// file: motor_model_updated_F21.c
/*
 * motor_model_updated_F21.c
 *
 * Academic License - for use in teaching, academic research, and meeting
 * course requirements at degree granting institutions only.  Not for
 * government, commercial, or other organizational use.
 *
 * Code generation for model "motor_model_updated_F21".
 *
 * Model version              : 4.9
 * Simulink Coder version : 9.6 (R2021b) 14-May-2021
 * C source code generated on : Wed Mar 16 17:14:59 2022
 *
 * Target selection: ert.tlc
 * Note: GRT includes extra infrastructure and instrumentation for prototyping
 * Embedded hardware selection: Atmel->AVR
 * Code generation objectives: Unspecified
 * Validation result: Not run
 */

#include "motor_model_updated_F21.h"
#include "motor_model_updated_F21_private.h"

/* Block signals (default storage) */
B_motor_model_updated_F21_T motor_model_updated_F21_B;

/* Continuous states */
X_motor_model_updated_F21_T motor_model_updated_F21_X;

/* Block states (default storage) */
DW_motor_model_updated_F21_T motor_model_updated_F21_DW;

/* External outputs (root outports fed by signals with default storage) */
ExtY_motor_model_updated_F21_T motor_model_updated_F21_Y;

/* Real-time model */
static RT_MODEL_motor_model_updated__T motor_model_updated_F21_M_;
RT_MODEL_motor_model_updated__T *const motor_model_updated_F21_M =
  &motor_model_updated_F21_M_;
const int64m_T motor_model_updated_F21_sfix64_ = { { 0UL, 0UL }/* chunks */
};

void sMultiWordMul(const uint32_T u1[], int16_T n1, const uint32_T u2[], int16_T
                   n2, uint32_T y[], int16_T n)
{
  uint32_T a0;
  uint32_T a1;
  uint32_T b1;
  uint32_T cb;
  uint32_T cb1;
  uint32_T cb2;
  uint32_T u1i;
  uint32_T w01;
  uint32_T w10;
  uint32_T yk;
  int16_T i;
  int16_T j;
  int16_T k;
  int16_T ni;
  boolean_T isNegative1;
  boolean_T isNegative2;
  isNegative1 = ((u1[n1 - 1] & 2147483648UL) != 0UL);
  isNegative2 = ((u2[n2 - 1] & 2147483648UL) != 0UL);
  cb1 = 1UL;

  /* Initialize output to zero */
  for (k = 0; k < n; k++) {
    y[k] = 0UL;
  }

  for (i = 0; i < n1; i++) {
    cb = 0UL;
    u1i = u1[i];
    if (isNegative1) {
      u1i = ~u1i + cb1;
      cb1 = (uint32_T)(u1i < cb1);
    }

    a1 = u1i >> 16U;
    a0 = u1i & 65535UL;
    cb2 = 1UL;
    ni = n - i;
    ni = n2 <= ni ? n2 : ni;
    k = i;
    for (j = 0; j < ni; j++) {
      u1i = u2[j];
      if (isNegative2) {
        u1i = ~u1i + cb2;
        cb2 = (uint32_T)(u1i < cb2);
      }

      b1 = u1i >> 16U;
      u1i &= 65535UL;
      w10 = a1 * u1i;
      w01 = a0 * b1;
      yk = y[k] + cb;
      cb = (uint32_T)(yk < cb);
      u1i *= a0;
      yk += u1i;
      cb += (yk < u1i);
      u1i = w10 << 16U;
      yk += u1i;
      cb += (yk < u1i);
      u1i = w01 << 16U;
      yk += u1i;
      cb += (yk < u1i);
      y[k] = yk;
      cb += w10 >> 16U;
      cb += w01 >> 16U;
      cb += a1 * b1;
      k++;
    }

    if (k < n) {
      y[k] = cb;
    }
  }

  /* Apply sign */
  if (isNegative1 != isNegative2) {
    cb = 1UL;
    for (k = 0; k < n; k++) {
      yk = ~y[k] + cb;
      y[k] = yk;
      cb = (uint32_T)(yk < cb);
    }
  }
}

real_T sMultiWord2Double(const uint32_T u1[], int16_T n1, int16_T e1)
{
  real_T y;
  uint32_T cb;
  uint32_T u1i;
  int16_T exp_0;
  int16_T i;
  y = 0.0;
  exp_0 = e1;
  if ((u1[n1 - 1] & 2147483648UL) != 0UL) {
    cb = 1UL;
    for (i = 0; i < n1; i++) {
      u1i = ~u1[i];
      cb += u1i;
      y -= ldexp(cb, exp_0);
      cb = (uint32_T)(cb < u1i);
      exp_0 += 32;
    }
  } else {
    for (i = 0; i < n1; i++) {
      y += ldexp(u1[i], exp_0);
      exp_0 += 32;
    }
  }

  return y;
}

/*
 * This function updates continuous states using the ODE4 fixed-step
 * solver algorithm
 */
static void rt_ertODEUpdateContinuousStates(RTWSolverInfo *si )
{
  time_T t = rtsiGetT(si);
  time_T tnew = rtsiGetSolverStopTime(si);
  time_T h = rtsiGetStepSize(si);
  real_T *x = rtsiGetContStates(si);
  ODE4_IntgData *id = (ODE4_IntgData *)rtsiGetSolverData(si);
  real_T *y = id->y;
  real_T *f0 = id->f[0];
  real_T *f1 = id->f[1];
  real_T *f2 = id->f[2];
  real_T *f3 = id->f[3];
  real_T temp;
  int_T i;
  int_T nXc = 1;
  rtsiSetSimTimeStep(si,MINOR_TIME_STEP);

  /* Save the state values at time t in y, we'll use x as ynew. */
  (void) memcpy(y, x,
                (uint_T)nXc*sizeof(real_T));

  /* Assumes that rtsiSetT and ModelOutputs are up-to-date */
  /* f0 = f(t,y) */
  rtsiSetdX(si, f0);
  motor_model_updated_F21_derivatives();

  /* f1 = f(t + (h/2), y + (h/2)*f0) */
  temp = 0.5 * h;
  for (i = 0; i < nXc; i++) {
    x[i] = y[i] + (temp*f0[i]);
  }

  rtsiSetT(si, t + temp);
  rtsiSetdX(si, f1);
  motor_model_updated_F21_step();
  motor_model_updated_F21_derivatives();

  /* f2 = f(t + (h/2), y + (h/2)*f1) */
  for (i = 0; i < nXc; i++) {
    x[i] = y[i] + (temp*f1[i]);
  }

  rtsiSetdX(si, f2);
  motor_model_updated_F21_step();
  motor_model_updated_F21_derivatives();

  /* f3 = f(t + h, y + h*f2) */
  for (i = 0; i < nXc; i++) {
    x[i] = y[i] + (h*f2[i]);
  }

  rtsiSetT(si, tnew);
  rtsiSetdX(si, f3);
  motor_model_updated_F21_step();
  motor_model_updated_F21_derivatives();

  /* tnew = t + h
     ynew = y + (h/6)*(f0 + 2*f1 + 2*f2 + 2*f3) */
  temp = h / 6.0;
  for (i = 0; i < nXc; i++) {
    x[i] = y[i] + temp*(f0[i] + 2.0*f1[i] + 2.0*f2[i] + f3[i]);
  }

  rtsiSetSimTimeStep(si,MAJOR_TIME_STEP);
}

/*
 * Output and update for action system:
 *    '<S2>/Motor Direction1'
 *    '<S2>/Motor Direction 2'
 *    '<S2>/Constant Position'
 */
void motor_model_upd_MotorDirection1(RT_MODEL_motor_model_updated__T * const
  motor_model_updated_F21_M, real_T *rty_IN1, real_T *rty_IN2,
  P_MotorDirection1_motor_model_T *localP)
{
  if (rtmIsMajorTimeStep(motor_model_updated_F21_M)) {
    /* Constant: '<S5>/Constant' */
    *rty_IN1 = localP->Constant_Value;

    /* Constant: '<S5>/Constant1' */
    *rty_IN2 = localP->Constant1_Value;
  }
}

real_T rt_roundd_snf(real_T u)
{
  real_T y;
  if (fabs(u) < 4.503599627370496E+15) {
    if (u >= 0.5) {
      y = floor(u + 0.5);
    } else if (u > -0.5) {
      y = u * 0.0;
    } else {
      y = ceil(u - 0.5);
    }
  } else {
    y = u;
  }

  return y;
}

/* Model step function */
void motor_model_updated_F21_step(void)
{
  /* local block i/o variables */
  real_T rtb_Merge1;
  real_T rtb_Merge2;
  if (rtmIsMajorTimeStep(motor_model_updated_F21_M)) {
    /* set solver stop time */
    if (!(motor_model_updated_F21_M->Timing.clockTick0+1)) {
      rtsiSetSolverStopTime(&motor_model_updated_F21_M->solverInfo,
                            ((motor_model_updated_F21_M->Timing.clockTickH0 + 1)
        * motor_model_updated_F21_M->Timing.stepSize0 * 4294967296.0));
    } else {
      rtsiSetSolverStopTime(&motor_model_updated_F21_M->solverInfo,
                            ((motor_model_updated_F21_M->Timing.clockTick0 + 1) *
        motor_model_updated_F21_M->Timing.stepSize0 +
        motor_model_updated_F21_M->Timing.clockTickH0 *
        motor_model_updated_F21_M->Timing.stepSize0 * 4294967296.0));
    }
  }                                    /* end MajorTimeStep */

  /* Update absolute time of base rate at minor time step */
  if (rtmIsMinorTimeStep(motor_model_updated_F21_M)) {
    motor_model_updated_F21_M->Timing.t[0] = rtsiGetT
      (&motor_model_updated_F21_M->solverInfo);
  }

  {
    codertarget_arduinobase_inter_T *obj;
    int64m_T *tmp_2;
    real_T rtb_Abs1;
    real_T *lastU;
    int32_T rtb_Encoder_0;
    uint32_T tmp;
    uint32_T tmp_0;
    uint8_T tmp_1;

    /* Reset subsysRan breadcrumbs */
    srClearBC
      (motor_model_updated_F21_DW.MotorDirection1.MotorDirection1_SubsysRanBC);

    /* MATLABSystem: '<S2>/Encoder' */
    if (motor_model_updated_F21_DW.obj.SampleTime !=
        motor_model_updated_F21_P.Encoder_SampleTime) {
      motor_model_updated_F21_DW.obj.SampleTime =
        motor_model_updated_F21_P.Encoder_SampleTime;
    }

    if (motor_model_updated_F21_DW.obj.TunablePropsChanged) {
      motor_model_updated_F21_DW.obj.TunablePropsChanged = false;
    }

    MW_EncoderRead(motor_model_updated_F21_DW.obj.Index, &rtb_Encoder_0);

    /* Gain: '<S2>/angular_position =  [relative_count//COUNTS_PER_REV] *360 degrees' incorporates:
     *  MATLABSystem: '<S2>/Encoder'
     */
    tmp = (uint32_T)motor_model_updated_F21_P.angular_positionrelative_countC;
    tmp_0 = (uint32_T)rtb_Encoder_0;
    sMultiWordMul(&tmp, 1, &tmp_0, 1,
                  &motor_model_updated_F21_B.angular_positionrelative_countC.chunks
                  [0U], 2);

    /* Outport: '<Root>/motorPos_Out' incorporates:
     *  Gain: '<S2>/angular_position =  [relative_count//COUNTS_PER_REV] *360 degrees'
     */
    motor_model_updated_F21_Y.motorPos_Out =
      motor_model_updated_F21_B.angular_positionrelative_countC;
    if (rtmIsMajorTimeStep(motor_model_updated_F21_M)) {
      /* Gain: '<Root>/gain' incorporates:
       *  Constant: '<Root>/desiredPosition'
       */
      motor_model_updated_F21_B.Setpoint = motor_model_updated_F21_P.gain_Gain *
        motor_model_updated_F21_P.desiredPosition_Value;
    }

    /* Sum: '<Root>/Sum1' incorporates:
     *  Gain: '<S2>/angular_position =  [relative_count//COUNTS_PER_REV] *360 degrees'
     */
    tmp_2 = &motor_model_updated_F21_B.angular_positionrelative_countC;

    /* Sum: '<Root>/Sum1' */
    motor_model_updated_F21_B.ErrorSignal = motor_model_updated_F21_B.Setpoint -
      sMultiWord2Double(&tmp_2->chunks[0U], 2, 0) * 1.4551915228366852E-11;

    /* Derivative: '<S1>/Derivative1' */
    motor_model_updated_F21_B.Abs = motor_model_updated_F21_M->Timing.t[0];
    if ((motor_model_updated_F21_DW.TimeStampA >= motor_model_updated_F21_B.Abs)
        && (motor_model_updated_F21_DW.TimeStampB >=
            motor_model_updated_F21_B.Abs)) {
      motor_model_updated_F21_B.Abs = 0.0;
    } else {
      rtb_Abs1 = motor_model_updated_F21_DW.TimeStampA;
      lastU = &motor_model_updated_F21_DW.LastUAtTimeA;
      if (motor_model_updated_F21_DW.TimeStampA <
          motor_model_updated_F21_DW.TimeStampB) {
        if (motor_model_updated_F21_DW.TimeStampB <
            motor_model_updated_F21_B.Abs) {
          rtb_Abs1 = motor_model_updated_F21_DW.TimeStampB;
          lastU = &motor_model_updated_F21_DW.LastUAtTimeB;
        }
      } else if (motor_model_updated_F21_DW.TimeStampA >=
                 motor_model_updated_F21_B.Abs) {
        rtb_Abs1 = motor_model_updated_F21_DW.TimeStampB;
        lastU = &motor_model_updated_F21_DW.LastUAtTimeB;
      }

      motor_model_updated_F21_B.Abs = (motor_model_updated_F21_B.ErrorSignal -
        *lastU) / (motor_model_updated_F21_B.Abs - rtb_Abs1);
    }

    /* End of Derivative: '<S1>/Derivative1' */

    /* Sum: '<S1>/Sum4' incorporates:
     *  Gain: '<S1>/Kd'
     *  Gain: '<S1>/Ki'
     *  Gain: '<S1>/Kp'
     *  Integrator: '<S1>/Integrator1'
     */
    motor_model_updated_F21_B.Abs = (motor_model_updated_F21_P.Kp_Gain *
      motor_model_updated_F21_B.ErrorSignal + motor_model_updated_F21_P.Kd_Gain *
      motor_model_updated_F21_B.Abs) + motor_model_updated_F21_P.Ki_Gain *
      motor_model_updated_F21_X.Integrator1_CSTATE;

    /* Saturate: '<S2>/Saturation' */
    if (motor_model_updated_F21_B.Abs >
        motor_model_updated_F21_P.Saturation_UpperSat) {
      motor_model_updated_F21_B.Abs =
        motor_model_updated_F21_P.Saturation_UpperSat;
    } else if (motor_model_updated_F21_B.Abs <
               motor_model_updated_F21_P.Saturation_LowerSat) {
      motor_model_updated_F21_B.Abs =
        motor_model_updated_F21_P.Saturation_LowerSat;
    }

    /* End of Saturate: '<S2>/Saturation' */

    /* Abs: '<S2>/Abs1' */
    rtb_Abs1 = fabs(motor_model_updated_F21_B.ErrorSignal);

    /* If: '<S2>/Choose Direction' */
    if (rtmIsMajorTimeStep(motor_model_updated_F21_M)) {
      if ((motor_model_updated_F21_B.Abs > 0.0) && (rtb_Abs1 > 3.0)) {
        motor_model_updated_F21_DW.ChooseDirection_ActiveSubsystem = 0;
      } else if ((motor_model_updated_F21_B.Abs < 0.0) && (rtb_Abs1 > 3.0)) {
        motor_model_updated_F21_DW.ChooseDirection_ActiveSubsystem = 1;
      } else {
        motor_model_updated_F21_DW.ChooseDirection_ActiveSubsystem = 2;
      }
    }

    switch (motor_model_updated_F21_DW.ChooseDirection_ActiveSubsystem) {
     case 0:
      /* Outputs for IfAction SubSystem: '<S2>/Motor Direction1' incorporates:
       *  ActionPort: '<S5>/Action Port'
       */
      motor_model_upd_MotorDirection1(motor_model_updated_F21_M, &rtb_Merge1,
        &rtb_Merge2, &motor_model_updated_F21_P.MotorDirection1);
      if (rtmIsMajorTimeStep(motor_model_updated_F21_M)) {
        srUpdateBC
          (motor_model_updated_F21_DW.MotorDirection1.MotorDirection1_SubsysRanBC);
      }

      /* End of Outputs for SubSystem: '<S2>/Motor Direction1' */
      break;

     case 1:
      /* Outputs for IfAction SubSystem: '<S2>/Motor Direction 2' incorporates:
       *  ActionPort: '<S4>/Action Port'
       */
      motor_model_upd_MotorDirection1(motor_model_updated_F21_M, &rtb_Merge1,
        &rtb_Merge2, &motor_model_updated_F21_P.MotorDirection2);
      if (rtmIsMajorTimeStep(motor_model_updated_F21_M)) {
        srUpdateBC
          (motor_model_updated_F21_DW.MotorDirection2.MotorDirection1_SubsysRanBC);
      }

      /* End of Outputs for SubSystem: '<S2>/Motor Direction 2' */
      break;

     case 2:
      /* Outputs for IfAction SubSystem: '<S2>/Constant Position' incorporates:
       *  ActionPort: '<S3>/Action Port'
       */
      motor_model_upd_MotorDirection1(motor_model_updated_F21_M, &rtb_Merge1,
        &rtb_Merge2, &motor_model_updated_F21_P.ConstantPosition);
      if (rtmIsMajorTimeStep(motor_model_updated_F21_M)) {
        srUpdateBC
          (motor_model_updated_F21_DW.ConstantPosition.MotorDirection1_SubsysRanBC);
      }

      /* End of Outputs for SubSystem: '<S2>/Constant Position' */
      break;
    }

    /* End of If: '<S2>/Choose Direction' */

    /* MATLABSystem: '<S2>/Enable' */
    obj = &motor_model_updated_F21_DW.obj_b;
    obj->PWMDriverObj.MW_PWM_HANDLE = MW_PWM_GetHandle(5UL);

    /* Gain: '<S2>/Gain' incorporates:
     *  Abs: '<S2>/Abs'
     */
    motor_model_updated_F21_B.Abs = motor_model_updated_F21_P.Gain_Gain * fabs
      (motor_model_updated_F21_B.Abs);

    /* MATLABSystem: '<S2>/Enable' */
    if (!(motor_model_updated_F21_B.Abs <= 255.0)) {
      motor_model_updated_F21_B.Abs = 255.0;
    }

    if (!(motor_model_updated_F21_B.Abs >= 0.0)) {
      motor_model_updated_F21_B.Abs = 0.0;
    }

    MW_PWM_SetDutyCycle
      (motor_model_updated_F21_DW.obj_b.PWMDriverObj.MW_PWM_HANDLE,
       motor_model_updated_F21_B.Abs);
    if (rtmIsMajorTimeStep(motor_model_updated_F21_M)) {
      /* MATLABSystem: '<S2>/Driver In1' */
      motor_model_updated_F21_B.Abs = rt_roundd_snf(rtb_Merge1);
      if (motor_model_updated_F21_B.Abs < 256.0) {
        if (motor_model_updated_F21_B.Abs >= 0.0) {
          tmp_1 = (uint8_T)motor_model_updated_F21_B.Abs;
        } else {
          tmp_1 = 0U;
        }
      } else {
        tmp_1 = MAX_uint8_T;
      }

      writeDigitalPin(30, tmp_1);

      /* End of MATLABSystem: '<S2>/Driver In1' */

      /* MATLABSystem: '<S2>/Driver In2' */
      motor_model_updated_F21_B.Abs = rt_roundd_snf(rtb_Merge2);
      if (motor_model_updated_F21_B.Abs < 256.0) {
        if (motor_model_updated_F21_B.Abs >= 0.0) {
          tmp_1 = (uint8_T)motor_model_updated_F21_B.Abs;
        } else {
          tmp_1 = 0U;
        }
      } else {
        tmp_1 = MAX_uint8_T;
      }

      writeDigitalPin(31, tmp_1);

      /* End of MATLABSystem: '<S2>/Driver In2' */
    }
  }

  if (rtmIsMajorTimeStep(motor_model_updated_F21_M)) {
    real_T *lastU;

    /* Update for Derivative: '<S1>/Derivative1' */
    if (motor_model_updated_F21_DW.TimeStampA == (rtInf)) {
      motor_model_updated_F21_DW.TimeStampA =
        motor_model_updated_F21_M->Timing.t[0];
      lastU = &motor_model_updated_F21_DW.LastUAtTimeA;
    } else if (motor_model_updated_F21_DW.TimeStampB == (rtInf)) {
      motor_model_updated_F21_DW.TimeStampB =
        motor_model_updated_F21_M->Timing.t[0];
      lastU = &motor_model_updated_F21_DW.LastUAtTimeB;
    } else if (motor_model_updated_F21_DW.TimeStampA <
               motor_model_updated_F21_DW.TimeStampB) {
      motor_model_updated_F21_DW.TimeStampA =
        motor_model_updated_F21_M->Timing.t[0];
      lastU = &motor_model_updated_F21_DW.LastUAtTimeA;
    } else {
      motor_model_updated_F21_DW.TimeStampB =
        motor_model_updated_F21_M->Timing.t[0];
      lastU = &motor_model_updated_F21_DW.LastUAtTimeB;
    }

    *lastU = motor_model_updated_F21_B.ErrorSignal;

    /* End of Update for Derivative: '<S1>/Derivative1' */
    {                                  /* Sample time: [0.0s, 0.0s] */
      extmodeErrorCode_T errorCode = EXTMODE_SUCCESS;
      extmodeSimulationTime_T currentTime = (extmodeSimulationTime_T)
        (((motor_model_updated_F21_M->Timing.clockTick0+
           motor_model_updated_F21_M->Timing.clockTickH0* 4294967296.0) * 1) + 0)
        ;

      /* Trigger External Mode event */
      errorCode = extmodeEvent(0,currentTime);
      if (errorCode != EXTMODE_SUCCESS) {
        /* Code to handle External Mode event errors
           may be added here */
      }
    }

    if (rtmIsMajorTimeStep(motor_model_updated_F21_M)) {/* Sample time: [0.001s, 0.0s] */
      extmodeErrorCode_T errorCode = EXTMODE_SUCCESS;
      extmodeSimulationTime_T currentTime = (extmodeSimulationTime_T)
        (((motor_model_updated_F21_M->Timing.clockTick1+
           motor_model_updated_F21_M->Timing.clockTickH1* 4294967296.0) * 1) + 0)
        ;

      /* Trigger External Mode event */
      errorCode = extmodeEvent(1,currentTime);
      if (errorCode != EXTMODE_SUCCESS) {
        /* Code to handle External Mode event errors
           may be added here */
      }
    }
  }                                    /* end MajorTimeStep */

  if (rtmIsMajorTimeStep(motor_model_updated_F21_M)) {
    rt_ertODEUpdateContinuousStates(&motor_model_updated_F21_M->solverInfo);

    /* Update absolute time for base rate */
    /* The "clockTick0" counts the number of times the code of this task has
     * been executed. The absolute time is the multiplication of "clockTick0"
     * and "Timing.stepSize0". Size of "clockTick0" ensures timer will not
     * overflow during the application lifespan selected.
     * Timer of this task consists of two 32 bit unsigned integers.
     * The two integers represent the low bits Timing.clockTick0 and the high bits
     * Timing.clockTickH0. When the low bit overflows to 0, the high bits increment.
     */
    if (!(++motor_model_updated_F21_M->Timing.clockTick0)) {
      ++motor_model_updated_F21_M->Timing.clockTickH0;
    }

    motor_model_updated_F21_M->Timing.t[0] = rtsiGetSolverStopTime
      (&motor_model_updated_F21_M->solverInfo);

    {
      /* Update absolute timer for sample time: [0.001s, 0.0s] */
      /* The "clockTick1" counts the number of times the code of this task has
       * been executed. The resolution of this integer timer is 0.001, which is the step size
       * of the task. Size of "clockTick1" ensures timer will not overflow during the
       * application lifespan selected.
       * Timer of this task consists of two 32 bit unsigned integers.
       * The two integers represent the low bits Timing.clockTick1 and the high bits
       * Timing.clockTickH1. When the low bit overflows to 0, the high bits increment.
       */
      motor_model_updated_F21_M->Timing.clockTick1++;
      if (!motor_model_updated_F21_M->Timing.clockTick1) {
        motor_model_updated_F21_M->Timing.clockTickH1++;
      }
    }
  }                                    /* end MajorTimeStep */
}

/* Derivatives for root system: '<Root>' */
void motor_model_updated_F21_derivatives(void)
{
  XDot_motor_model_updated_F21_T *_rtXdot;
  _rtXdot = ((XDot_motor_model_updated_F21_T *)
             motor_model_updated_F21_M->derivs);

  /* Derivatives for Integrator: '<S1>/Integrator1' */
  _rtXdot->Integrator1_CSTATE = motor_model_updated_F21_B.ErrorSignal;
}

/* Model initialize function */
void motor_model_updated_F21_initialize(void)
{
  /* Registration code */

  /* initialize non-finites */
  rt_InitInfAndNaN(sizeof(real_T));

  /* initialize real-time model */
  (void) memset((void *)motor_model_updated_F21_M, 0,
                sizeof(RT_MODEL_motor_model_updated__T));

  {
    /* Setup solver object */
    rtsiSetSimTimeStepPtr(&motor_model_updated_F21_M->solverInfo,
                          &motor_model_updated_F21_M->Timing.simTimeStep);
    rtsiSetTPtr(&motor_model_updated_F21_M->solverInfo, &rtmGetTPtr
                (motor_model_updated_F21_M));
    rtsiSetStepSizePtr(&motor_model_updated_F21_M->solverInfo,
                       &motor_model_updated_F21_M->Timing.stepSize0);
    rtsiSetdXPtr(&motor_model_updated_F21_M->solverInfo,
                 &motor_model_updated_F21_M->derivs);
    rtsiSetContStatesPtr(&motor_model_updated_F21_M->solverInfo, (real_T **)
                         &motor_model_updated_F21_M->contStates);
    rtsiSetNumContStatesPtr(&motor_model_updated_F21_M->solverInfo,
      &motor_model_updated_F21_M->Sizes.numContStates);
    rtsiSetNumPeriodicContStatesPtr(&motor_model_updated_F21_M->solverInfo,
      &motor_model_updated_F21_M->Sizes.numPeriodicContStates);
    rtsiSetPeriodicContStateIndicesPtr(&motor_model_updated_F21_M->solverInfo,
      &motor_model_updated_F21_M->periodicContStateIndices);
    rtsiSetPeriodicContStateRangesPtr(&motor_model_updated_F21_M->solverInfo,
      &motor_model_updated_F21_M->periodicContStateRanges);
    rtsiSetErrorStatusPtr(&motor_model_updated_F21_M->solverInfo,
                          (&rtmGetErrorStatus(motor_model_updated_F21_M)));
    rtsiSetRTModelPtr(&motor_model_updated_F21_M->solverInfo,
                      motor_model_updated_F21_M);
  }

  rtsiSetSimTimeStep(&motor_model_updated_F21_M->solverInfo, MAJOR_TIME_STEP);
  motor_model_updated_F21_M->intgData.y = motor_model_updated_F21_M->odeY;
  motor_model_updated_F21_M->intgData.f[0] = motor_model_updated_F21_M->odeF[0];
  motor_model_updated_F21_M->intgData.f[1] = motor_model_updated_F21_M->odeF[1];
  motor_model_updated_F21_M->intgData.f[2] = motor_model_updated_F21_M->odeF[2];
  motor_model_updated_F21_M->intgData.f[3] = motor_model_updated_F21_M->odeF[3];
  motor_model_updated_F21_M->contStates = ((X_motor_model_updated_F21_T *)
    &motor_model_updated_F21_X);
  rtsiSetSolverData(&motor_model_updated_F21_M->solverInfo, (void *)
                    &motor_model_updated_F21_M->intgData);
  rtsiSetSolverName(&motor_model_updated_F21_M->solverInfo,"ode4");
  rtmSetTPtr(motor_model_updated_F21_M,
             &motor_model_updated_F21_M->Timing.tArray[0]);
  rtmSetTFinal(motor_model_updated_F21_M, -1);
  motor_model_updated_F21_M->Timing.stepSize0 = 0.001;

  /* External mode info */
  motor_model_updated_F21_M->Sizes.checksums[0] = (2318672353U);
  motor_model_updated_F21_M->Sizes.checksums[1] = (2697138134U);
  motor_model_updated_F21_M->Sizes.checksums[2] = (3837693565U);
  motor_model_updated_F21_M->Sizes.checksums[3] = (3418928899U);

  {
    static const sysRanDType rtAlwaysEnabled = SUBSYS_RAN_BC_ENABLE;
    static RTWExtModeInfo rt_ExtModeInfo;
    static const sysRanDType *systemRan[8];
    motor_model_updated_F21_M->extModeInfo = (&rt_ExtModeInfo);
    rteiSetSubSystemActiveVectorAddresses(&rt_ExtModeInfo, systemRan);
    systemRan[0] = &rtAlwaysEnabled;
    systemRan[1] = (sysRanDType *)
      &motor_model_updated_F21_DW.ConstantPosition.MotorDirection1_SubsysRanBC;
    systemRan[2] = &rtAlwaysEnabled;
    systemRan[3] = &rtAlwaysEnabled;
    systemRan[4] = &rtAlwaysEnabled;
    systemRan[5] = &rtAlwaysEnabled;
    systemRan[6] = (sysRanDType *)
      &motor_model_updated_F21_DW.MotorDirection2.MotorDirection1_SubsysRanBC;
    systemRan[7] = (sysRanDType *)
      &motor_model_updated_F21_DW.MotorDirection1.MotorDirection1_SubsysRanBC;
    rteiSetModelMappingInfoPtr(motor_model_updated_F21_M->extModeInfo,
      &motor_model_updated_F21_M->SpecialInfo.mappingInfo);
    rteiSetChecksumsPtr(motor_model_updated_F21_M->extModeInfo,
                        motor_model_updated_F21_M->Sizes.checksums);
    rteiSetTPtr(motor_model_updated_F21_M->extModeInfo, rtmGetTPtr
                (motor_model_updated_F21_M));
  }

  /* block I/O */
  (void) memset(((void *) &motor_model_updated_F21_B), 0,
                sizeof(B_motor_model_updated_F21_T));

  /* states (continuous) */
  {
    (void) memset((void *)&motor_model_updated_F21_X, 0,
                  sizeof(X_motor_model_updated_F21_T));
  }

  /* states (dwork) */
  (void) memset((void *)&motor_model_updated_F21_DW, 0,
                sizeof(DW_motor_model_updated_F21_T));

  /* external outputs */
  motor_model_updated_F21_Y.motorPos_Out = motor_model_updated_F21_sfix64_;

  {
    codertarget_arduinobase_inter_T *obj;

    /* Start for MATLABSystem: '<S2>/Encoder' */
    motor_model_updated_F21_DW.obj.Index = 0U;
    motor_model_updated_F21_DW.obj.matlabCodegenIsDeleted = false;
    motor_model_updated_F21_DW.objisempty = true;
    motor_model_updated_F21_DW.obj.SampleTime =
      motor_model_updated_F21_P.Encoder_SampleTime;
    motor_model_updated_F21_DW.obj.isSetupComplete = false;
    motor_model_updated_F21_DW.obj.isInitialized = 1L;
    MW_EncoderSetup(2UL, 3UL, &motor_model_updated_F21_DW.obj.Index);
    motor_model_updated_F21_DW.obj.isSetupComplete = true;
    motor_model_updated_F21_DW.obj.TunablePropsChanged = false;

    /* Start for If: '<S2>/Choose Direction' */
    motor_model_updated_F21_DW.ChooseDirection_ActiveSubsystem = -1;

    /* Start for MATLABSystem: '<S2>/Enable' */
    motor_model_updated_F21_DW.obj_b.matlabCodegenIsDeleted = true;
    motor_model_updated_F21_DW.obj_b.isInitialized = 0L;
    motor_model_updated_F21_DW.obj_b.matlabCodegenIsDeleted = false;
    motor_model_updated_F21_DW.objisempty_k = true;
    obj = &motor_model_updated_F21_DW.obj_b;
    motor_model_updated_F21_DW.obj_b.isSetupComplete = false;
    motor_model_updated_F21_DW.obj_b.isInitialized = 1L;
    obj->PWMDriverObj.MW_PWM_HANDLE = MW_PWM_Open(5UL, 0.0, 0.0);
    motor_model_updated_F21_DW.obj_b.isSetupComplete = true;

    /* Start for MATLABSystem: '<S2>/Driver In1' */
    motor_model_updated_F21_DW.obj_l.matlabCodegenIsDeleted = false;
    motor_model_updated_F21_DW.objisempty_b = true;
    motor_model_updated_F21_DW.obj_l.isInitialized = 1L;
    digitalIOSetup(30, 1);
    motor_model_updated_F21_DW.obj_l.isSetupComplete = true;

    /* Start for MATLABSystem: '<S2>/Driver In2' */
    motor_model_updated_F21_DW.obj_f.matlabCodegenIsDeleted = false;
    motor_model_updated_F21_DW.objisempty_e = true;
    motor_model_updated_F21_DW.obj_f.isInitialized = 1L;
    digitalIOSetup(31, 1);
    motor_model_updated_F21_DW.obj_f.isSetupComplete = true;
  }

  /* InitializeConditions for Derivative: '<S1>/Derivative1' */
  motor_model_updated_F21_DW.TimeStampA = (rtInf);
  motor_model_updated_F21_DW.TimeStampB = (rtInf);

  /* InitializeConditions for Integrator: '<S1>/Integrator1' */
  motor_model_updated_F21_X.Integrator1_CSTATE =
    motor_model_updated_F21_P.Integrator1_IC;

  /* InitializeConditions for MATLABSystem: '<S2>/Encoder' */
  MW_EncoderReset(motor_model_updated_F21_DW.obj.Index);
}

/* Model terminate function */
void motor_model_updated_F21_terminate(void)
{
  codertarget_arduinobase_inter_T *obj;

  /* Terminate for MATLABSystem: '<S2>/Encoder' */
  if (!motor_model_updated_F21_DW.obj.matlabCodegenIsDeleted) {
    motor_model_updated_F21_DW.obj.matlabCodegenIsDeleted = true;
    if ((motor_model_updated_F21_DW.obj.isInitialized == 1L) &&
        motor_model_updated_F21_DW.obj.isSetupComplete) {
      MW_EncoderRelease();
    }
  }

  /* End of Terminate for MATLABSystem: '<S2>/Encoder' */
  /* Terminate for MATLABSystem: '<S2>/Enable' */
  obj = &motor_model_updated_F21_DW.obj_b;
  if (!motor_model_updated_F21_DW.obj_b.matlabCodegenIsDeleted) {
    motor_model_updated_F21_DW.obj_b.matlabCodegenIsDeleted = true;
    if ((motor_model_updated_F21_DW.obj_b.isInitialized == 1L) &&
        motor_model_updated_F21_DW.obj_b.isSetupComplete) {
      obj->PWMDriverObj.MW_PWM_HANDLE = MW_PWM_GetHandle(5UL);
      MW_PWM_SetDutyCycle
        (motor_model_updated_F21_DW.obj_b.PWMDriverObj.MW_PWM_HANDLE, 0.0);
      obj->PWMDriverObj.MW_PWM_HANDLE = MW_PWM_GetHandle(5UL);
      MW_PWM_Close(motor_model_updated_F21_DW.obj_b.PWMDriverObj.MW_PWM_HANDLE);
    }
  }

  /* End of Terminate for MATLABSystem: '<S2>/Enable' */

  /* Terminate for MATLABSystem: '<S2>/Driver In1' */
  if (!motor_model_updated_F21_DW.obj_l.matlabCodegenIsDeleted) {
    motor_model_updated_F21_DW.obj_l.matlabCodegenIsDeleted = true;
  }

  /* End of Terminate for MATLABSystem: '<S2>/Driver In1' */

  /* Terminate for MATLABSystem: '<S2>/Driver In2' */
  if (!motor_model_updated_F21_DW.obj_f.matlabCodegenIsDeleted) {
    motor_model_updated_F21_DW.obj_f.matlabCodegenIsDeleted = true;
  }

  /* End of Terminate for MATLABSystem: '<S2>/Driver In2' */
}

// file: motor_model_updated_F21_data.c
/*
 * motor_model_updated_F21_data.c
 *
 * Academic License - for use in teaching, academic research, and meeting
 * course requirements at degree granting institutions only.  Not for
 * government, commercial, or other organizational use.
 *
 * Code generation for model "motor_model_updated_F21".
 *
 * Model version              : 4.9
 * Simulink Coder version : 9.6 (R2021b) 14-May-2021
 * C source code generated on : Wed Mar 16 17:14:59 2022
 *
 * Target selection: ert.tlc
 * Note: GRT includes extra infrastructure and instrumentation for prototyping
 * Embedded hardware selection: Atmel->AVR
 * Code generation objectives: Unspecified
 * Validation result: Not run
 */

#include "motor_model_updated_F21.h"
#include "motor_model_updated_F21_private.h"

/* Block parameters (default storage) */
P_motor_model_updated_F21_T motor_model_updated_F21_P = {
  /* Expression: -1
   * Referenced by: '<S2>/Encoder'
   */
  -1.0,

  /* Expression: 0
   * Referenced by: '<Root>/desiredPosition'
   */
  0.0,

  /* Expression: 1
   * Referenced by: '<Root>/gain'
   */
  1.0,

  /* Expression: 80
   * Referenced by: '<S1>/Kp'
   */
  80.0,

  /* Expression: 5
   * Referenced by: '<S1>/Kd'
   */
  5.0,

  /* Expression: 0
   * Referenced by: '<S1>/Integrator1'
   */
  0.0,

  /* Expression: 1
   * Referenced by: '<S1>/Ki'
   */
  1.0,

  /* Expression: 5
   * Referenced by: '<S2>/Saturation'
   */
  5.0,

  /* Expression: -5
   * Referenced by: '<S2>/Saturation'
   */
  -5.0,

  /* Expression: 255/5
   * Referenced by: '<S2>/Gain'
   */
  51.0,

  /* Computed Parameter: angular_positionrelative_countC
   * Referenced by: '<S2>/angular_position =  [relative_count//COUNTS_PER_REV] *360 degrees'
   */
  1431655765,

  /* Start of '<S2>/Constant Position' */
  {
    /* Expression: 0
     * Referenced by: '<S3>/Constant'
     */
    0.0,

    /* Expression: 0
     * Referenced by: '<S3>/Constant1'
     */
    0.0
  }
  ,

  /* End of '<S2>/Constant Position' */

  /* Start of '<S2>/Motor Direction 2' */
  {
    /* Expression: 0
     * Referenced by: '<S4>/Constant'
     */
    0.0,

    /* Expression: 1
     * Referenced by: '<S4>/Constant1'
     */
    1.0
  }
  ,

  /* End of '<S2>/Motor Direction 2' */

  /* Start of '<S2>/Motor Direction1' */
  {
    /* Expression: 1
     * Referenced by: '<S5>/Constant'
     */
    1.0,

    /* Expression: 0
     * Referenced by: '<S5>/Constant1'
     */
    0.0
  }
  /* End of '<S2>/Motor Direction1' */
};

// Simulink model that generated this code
simulink model "motor_model_updated_F21"  (R2021b)
settings: Solver=ode4  StartTime=0.0  StopTime=inf  FixedStep=0.001  RelTol=1e-3  EnableMultiTasking=on
model workspace (MAT data in the model file):
  Error = 0
libraries: arduinolib x3, arduinosensorlib x1

== system motor_model_updated_F21 ==
  Controller : Subsystem
  Display : Display
  Motor : Subsystem
  Sum1 : Sum  Inputs=|+-
  desiredPosition : Constant  Value=0
  gain : Gain
  motorPos_Out : Outport  VectorParamsAs1DForOutWhenUnconnected=off
  wires:
  gain/1 -> Sum1/1  "Setpoint"
  Motor/1(position in degrees) -> Sum1/2, motorPos_Out/1, Display/1  "Motor Position"
  Controller/1(unfiltered control input) -> Motor/1(unfiltered control input)
  Sum1/1 -> Motor/2(unfiltered control input1), Controller/1(error signal)  "Error Signal"
  desiredPosition/1 -> gain/1

== system motor_model_updated_F21/Controller ==
  note: Adjust these gains and observe the change of the
      | motor response on the Error and Motor Position
      | plots.
  error signal : Inport
  Derivative1 : Derivative
  Integrator1 : Integrator
  Kd : Gain  Gain=5
  Ki : Gain
  Kp : Gain  Gain=80
  Sum4 : Sum  Inputs=||+++
  unfiltered control input : Outport
  wires:
  Kd/1 -> Sum4/2
  Integrator1/1 -> Ki/1
  Ki/1 -> Sum4/3
  Derivative1/1 -> Kd/1
  error signal/1 -> Derivative1/1, Integrator1/1, Kp/1  "Error Signal"
  Kp/1 -> Sum4/1
  Sum4/1 -> unfiltered control input/1

== system motor_model_updated_F21/Motor ==
  note: The counter works by triggering an interrupt from encoder A
      | on the rising edge. It then uses the value from encoder B to
      | determine what direction the motor is turning. Review how
      | quadrature encoders use gray code if you're rusty on that!
  note: PWM block takes value b/w 0-255 representing
      | 0%-100% duty cycle. This gain block scales the
      | output voltage based on the error. The motor will
      | move more slowly as the error grows
      | smaller. The scale is based on the thresholds
      | of the saturation block.
  note: Outputs analog voltage to control position of DC motor
      |
      | Encoder feedback from motor calculated using interrupt pins on the Arduino
      |
      | Helpful (but not necessary) to convert encoder ticks to degrees using the
      | gain block
  note: Saturation
  note: How to drive motor:
      | Drive enable pin with PWM signal
      | Provide high signal to IN pin on motor driver
      | Provide low signal to following IN pin on the motor driver
      |
      | Example:
      | Connect pins 30&31 to IN1 and IN2 on motor driver
      | Driving pin 30 high and pin 31 low will cause the motor to spin one direction
      | Reversing pins 30 and 31 will cause the motor to spin the other direction
  note: The hall sensors should be connected to pins 2&3 of the
      | Arduino. Having A connected to pin 2 and B connected to
      | pin 3 will spin the motor one way, and reversing them will
      | spin the motor the opposite way.
  unfiltered control input : Inport
  unfiltered control input1 : Inport  Port=2
  Abs : Abs
  Abs1 : Abs
  Choose Direction : If  NumInputs=2  IfExpression=u1 > 0 & u2 > 3  ElseIfExpressions=u1 < 0 & u2 > 3
  Constant Position : Subsystem  TreatAsAtomicUnit=on
  Driver In1 : arduinolib/Digital Output  pinNumber=30  Direction=output  blockPlatform=arduino
  Driver In2 : arduinolib/Digital Output  pinNumber=31  Direction=output  blockPlatform=arduino
  Enable : arduinolib/PWM  pinNumber=5  frequencyType=Default  desiredFrequency=490.2  achievableFrequency=490.2
  Encoder : arduinosensorlib/Encoder  InputA=2  InputB=3  Mode=No reset  SampleTime=-1
  Gain : Gain  Gain=255/5
  Merge1 : Merge  Inputs=3
  Merge2 : Merge  Inputs=3
  Motor Direction 2 : Subsystem  TreatAsAtomicUnit=on
  Motor Direction1 : Subsystem  TreatAsAtomicUnit=on
  Saturation : Saturate  UpperLimit=5  LowerLimit=-5
  angular_position = [relative_count/COUNTS_PER_REV] *360 degrees : Gain  Gain=360/17280
  position in degrees : Outport  VectorParamsAs1DForOutWhenUnconnected=off
  wires:
  angular_position = [relative_count/COUNTS_PER_REV] *360 degrees/1 -> position in degrees/1
  unfiltered control input/1 -> Saturation/1
  Saturation/1 -> Abs/1, Choose Direction/1
  Choose Direction/1 -> Motor Direction1/Action
  Motor Direction1/1(IN1) -> Merge1/1
  Motor Direction 2/1(IN1) -> Merge1/2
  Motor Direction1/2(IN2) -> Merge2/1
  Motor Direction 2/2(IN2) -> Merge2/2
  Abs/1 -> Gain/1
  Gain/1 -> Enable/1
  Merge1/1 -> Driver In1/1
  Merge2/1 -> Driver In2/1
  Constant Position/2(IN2) -> Merge2/3
  Constant Position/1(IN1) -> Merge1/3
  unfiltered control input1/1 -> Abs1/1
  Abs1/1 -> Choose Direction/2
  Choose Direction/3 -> Constant Position/Action
  Choose Direction/2 -> Motor Direction 2/Action
  Encoder/1 -> angular_position = [relative_count/COUNTS_PER_REV] *360 degrees/1

== system motor_model_updated_F21/Motor/Constant Position ==
  Action Port : ActionPort  ActionPortLabel=else
  Constant : Constant  Value=0
  Constant1 : Constant  Value=0
  IN1 : Outport
  IN2 : Outport  Port=2
  wires:
  Constant/1 -> IN1/1
  Constant1/1 -> IN2/1

== system motor_model_updated_F21/Motor/Motor Direction 2 ==
  Action Port : ActionPort  ActionPortLabel=elseif(u1 < 0 & u2 > 3)
  Constant : Constant  Value=0
  Constant1 : Constant
  IN1 : Outport
  IN2 : Outport  Port=2
  wires:
  Constant/1 -> IN1/1
  Constant1/1 -> IN2/1

== system motor_model_updated_F21/Motor/Motor Direction1 ==
  Action Port : ActionPort  ActionPortLabel=if(u1 > 0 & u2 > 3)
  Constant : Constant
  Constant1 : Constant  Value=0
  IN1 : Outport
  IN2 : Outport  Port=2
  wires:
  Constant/1 -> IN1/1
  Constant1/1 -> IN2/1
